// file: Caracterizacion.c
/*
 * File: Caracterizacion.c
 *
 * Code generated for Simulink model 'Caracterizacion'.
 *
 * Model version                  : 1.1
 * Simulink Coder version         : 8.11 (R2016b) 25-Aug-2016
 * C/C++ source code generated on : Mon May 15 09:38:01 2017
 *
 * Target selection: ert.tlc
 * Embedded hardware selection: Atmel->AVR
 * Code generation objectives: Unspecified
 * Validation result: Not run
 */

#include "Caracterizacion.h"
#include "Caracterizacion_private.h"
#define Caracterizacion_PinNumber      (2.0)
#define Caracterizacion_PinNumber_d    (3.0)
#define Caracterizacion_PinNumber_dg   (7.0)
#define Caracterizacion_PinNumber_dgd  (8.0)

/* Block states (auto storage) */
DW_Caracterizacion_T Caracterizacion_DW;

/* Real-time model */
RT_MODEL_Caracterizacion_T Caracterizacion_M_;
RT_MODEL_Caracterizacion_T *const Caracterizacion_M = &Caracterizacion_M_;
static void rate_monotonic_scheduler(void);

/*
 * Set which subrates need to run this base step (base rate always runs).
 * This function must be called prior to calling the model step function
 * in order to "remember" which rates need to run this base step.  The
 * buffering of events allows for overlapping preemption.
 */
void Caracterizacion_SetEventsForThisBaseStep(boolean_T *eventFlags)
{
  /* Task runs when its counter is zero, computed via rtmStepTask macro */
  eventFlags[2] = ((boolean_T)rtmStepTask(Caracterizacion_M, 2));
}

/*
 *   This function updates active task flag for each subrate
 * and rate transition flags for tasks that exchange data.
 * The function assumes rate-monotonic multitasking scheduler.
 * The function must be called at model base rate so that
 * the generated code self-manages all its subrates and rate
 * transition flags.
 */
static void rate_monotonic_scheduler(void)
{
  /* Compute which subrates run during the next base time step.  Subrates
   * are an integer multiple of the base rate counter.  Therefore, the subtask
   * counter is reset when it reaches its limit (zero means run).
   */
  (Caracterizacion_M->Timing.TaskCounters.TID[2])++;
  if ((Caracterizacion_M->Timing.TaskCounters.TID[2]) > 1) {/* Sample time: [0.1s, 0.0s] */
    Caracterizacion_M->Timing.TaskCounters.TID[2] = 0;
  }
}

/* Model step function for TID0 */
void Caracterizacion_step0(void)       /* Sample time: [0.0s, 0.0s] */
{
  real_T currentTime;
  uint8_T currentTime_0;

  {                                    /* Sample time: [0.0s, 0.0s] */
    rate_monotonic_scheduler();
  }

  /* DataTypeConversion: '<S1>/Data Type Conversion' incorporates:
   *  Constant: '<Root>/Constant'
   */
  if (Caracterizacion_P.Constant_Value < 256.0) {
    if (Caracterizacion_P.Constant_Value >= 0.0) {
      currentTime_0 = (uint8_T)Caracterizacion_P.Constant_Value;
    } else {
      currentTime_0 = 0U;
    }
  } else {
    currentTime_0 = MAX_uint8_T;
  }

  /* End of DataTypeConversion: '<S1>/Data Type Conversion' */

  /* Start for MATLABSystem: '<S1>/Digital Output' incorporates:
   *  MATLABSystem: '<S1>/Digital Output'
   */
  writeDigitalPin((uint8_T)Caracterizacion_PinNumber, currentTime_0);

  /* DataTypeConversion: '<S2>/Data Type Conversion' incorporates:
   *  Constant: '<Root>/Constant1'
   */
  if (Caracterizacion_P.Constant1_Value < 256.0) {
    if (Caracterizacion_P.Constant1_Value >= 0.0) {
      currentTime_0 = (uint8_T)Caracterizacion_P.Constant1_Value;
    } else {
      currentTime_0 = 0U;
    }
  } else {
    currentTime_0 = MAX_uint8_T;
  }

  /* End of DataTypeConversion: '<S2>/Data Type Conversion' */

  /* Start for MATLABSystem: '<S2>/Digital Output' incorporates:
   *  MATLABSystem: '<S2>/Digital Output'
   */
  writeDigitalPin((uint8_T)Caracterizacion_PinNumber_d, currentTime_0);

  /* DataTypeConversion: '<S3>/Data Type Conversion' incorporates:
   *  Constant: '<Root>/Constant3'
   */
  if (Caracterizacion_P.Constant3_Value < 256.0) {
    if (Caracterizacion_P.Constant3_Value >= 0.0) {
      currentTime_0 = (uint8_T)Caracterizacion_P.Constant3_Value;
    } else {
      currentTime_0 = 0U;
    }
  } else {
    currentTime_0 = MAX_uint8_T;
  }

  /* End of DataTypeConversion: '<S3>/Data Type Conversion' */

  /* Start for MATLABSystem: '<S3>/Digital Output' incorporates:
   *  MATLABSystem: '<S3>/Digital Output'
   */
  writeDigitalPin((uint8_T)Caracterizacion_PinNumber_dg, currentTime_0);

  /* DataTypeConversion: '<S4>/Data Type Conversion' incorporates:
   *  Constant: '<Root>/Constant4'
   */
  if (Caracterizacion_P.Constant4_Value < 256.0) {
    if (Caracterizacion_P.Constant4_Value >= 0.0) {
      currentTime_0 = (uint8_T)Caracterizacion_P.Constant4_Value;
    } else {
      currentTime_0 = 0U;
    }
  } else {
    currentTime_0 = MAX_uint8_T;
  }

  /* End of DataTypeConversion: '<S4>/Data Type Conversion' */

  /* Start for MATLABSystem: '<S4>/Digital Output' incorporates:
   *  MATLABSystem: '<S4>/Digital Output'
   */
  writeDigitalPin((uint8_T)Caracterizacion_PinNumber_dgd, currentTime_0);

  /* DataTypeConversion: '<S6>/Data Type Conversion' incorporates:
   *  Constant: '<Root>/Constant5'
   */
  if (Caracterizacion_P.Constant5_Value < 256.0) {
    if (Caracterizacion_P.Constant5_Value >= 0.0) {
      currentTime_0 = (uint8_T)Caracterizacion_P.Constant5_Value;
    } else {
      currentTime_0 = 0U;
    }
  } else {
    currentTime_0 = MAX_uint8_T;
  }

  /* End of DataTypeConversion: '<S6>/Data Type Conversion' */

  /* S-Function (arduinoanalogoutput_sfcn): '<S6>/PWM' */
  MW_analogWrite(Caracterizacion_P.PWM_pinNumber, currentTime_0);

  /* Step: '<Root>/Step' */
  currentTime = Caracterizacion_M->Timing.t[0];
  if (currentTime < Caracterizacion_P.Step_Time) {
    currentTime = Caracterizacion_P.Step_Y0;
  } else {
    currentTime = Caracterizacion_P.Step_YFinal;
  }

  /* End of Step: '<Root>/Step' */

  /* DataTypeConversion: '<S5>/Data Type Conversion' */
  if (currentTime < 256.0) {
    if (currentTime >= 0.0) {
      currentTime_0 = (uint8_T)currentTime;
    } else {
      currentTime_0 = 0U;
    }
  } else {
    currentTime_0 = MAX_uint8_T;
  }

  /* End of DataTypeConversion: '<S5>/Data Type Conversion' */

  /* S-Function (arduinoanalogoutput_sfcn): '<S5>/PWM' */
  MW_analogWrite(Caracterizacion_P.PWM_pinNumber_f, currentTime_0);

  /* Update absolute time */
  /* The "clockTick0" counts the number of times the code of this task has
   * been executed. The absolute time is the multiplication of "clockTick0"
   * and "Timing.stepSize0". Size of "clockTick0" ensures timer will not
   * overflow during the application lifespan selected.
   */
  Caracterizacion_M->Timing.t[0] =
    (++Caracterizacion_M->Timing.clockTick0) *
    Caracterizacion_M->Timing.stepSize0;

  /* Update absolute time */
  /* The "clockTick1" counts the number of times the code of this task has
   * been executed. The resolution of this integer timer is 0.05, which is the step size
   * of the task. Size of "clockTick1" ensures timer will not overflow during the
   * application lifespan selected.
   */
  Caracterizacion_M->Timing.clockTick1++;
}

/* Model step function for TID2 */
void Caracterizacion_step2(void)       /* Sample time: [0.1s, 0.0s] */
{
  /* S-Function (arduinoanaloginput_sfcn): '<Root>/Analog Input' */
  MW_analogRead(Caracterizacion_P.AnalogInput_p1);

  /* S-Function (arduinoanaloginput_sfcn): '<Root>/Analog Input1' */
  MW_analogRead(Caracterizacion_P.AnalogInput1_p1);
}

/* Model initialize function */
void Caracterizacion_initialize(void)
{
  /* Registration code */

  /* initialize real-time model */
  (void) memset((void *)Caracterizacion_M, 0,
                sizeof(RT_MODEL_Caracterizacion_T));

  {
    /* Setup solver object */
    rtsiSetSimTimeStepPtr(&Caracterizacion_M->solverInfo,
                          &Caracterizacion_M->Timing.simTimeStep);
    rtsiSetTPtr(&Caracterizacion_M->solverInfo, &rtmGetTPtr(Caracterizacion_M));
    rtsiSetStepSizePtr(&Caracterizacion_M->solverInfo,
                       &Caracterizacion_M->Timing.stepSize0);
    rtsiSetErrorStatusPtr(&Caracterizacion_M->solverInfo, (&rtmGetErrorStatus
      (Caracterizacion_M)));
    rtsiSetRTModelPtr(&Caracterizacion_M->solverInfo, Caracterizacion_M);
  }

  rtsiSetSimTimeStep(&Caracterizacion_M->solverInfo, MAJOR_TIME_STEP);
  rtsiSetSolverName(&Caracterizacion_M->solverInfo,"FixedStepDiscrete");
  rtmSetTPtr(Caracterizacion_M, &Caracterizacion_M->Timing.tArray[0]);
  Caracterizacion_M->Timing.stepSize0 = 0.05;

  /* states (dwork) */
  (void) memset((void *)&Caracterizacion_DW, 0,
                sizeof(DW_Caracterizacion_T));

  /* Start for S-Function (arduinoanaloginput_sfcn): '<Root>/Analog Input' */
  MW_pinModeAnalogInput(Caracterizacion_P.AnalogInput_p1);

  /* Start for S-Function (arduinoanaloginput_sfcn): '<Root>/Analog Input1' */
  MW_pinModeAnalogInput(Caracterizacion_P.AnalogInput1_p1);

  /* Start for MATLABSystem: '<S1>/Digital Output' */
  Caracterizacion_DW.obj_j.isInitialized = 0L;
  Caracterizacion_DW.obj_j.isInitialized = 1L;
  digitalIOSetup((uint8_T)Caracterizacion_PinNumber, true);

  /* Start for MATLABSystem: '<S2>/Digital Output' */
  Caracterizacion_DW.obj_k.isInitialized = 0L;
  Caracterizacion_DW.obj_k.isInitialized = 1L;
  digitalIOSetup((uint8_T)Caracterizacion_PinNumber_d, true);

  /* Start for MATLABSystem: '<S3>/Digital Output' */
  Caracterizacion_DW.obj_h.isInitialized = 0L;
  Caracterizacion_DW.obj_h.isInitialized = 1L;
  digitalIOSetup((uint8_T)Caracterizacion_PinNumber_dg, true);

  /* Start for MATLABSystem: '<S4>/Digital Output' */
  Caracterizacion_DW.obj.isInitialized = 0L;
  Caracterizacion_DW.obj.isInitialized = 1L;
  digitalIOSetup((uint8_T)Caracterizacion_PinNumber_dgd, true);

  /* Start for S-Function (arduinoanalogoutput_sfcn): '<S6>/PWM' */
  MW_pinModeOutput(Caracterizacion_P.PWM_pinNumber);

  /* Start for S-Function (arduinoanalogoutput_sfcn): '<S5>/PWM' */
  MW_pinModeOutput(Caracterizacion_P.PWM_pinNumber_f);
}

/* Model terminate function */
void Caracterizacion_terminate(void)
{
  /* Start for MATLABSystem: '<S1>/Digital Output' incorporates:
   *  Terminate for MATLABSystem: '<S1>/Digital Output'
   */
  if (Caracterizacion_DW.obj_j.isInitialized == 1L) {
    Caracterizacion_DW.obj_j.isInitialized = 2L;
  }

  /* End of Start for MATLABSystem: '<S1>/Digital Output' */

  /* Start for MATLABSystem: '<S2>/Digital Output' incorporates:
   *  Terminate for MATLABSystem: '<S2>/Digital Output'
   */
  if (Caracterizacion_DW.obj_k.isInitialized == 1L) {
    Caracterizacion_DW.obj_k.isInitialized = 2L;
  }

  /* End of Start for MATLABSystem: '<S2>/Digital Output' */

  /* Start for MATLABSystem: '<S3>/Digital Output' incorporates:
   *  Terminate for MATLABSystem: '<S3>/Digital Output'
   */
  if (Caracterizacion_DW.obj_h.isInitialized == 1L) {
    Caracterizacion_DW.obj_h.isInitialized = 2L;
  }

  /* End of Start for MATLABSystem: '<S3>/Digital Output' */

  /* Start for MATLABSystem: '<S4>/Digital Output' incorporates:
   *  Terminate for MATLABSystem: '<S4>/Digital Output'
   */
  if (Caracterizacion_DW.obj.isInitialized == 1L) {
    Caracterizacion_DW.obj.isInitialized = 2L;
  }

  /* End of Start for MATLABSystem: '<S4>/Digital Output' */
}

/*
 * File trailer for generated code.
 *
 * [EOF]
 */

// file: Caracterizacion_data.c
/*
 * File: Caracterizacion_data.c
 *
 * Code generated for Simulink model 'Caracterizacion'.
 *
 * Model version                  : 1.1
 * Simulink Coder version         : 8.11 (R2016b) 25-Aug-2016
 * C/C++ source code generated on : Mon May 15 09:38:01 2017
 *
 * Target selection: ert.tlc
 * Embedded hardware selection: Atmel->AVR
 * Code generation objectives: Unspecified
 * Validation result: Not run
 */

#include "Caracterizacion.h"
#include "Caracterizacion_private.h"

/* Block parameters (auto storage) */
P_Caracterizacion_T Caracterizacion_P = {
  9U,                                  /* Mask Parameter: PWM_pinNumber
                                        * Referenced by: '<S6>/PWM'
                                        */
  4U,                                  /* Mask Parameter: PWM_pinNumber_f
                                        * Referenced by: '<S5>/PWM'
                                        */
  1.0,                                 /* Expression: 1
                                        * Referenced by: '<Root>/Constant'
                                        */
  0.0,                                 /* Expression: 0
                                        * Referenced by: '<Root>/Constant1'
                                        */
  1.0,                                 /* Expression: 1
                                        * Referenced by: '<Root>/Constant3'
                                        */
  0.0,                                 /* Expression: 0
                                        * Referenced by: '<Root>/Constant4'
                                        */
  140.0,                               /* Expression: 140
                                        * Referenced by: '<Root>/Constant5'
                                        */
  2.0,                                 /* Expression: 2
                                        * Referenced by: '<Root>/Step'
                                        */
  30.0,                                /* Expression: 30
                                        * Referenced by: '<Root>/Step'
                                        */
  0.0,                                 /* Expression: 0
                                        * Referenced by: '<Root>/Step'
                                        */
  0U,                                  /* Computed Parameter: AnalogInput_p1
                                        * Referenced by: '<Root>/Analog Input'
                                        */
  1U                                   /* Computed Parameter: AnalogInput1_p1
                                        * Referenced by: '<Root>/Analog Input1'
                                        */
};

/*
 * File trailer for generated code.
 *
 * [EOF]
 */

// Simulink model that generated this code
simulink model "Caracterizacion"  (R2016b)
settings: Solver=FixedStepDiscrete  StartTime=0.0  StopTime=20  FixedStep=0.05  RelTol=1e-3  EnableMultiTasking=on
libraries: arduinolib x8

== system Caracterizacion ==
  Analog Input : arduinolib/Analog Input  pinNumber=0  sampleTime=0.1  blockPlatform=arduino
  Analog Input1 : arduinolib/Analog Input  pinNumber=1  sampleTime=0.1  blockPlatform=arduino
  Constant : Constant
  Constant1 : Constant  Value=0
  Constant3 : Constant
  Constant4 : Constant  Value=0
  Constant5 : Constant  Value=140
  Digital Output : arduinolib/Digital Output  pinNumber=2  blockPlatform=arduino
  Digital Output1 : arduinolib/Digital Output  pinNumber=3  blockPlatform=arduino
  Digital Output2 : arduinolib/Digital Output  pinNumber=7  blockPlatform=arduino
  Digital Output3 : arduinolib/Digital Output  pinNumber=8  blockPlatform=arduino
  PWM : arduinolib/PWM  pinNumber=4  blockPlatform=arduino
  PWM1 : arduinolib/PWM  pinNumber=9  blockPlatform=arduino
  Scope : Scope
  Scope1 : Scope
  Step : Step  Time=2  Before=30  After=0  SampleTime=0
  wires:
  Analog Input/1 -> Scope/1
  Analog Input1/1 -> Scope1/1
  Constant/1 -> Digital Output/1
  Constant1/1 -> Digital Output1/1
  Constant3/1 -> Digital Output2/1
  Constant4/1 -> Digital Output3/1
  Constant5/1 -> PWM1/1
  Step/1 -> PWM/1
